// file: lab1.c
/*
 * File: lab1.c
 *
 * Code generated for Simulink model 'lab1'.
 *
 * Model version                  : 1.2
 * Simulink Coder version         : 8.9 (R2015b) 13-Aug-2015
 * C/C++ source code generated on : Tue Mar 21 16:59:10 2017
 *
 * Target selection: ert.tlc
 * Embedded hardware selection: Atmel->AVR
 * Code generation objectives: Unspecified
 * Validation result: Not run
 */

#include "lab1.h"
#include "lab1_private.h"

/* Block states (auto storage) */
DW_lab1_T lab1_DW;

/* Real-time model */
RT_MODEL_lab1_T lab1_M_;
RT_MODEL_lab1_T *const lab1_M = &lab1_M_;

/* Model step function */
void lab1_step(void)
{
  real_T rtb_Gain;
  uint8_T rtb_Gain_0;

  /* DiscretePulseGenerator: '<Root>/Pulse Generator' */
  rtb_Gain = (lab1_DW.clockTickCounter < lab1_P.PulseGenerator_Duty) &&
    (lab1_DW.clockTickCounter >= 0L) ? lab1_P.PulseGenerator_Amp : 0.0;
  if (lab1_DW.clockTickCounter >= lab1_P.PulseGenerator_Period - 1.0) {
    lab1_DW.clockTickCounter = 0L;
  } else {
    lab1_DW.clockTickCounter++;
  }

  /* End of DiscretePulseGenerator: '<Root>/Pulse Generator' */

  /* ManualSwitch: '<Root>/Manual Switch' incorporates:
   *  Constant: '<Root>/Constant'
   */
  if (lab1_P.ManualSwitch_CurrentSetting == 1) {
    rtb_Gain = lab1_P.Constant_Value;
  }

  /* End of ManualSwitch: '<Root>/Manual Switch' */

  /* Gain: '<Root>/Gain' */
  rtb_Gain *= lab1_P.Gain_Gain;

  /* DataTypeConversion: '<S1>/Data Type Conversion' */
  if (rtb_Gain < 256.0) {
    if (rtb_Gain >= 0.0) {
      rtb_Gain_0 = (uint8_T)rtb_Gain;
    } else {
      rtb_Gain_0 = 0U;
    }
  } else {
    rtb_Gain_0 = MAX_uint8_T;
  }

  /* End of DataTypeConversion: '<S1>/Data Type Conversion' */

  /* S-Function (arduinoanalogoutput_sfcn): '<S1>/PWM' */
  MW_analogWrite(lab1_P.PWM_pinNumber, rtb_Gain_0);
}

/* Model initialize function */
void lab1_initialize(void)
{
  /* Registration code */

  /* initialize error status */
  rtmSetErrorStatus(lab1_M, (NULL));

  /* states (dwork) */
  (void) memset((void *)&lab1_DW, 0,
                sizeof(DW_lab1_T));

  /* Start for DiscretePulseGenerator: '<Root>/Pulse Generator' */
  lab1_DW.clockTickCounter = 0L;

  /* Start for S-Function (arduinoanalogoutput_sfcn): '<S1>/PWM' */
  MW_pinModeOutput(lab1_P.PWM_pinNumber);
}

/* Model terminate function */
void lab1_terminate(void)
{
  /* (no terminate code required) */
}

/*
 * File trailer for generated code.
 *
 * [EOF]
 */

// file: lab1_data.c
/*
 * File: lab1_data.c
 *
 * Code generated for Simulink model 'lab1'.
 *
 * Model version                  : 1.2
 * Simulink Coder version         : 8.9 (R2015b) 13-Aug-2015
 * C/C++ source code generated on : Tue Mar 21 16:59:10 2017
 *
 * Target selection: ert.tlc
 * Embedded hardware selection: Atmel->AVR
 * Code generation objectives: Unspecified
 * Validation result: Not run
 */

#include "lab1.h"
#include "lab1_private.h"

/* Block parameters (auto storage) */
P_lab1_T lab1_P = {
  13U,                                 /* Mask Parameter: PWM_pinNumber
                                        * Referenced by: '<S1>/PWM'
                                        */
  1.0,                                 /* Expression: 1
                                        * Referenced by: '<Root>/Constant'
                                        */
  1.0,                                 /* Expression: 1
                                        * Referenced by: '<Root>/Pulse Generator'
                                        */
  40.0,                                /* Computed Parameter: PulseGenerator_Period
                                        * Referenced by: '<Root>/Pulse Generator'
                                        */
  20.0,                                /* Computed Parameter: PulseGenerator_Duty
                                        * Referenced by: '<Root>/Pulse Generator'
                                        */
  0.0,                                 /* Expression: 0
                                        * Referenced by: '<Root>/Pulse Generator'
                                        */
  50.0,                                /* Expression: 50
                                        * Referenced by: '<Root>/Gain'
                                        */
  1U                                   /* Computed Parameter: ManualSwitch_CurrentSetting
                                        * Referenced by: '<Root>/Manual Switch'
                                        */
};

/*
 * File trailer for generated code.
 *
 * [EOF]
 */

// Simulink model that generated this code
simulink model "lab1"  (R2015b)
settings: Solver=FixedStepDiscrete  StartTime=0.0  StopTime=inf  FixedStep=0.05  RelTol=1e-3
libraries: arduinolib x1

== system lab1 ==
  Constant : Constant
  Gain : Gain  Gain=50
  Manual Switch : ManualSwitch  CurrentSetting=0
  PWM : arduinolib/PWM  pinNumber=13  blockPlatform=arduino
  Pulse Generator : DiscretePulseGenerator  PulseType=Time based  PulseWidth=50
  wires:
  Pulse Generator/1 -> Manual Switch/2
  Constant/1 -> Manual Switch/1
  Manual Switch/1 -> Gain/1
  Gain/1 -> PWM/1
